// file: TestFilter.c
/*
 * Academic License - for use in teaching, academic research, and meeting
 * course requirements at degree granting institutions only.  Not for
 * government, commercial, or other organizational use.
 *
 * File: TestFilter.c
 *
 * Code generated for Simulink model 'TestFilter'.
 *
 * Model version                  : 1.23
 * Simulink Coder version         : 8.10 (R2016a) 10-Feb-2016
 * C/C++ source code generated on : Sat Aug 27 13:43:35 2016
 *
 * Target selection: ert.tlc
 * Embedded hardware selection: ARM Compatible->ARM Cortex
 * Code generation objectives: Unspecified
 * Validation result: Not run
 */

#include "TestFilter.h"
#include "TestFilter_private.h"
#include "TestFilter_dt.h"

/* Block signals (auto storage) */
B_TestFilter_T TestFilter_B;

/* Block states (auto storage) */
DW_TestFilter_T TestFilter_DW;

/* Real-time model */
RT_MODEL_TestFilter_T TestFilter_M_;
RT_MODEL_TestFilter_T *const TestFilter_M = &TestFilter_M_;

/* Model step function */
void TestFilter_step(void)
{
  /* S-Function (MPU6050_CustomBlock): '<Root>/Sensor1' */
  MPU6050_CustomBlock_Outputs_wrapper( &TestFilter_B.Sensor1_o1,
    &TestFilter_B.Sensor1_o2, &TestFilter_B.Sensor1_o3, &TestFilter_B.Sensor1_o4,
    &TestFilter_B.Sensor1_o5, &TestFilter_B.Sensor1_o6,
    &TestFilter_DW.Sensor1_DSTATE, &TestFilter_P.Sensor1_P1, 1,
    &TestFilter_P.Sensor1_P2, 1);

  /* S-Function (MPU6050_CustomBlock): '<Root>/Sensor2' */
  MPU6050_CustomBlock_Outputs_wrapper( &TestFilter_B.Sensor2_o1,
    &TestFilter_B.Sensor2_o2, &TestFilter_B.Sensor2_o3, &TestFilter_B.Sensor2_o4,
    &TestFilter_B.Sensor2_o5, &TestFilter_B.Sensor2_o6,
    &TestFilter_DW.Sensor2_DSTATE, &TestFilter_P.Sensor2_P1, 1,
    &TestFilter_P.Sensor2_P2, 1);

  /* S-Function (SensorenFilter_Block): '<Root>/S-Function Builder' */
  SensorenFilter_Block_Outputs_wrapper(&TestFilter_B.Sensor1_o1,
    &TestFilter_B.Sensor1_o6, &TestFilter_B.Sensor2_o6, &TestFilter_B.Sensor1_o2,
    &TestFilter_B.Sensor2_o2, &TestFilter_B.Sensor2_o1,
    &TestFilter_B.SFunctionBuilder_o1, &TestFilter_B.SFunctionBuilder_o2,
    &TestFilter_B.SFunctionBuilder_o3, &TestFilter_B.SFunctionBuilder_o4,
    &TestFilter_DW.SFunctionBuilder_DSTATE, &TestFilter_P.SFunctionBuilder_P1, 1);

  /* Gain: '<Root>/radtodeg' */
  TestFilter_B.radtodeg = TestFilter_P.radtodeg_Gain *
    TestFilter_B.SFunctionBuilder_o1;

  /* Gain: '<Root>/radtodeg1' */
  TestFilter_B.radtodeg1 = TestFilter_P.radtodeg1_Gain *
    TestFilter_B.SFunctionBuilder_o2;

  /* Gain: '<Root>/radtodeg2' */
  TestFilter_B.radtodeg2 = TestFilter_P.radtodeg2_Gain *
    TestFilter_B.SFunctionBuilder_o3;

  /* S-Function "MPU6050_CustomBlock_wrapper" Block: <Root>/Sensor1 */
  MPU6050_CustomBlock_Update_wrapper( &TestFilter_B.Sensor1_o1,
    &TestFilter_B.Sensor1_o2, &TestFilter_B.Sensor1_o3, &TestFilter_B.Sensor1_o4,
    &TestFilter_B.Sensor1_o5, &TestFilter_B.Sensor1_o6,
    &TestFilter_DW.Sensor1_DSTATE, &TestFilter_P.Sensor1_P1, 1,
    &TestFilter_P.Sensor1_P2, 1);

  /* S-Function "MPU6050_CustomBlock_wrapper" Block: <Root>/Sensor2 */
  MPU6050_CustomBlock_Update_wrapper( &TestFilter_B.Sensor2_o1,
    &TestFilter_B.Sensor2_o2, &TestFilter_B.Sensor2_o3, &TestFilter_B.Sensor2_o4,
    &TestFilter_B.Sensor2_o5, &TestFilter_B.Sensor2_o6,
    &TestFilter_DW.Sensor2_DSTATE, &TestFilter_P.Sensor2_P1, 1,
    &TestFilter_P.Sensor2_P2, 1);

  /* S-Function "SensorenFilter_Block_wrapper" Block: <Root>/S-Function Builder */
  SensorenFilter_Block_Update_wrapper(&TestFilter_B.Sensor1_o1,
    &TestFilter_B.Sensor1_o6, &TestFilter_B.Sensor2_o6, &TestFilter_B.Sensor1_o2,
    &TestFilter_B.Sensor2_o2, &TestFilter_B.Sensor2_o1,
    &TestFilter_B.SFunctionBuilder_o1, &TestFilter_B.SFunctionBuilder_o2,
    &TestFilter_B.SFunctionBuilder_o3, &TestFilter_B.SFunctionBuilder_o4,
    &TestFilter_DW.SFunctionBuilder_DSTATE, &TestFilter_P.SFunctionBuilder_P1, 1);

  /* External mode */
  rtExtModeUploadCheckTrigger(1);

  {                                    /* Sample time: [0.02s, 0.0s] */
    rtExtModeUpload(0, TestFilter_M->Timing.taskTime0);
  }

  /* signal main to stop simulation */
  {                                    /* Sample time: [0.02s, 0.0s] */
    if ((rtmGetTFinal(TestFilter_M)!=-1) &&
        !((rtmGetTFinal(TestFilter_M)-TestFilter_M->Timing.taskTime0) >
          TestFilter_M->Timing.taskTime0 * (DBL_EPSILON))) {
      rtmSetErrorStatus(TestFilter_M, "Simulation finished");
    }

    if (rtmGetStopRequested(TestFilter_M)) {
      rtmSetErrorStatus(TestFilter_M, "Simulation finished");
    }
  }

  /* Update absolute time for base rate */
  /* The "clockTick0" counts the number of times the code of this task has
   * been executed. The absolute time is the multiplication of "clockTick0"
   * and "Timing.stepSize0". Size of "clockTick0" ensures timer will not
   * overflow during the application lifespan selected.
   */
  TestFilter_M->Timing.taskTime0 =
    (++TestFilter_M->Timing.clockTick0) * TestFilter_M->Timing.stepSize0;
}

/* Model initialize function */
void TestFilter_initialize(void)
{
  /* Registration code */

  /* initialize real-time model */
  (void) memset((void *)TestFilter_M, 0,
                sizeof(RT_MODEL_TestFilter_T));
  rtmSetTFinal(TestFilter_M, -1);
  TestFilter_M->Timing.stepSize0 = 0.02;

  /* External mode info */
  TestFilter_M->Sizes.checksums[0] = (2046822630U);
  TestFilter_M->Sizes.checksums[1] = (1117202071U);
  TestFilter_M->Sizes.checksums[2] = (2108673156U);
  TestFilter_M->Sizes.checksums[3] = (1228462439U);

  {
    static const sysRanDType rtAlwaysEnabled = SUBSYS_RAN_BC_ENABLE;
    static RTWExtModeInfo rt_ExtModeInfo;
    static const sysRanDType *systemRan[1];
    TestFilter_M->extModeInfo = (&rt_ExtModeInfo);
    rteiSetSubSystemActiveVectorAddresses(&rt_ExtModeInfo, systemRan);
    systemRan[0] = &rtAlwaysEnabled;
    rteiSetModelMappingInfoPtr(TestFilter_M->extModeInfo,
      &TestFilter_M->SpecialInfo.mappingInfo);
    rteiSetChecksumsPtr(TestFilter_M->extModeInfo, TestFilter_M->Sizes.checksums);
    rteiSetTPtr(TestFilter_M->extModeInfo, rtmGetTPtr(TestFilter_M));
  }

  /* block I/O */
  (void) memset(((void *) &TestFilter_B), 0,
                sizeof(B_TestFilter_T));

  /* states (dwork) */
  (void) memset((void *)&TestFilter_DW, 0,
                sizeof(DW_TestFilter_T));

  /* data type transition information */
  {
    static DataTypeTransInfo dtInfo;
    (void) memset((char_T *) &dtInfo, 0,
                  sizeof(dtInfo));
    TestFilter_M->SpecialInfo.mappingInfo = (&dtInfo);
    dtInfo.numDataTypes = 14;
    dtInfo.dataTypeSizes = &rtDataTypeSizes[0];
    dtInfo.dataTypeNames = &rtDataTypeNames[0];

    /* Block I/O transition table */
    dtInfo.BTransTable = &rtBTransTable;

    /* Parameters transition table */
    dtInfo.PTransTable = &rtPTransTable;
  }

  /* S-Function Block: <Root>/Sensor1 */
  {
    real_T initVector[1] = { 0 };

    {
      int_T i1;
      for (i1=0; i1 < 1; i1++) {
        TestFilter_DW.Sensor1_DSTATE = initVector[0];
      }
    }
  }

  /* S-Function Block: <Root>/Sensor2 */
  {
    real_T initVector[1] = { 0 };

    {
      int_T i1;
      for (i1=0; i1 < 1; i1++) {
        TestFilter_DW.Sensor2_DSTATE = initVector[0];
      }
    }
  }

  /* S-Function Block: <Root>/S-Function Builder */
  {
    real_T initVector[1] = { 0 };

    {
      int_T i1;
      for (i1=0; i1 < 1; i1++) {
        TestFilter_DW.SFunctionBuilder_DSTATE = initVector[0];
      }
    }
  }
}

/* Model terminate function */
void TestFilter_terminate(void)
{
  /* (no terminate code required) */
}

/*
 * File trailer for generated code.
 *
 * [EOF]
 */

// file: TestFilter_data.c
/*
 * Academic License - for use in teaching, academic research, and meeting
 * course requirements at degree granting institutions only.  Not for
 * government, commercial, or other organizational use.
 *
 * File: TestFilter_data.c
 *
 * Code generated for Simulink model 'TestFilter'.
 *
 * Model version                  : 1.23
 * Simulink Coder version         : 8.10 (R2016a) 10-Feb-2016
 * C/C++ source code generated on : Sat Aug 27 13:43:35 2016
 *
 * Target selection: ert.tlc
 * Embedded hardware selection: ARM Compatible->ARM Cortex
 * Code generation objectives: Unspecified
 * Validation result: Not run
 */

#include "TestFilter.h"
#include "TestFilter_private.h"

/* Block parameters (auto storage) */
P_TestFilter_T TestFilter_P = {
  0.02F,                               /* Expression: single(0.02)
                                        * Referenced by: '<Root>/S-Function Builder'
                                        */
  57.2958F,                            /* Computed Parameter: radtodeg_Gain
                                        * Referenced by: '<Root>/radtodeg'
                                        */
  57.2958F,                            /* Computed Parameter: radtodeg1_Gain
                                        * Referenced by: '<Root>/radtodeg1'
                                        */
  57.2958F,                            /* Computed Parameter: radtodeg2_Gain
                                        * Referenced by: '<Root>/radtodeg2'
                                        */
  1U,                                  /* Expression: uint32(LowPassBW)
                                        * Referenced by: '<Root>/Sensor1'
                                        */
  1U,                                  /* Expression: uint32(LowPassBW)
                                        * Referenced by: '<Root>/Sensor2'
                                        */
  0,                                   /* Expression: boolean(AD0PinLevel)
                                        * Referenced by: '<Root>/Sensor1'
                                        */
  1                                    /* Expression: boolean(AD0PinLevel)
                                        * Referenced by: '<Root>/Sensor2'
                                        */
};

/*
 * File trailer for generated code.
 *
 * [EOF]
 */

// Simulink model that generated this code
simulink model "TestFilter"  (R2016a)
settings: Solver=FixedStepDiscrete  StartTime=0.0  StopTime=inf  FixedStep=0.02  RelTol=1e-3

== system TestFilter ==
  S-Function Builder : S-Function  InitFcn=try, set_param(gcb,'FunctionName','SensorenFilter_Block'), end  FunctionName=SensorenFilter_Block  Parameters=single(0.02)  SFunctionModules=SensorenFilter_Block_wrapper  SFunctionDeploymentMode=off  EnableBusSupport=off  mask(S-Function Builder){}
      mask help: Simulink:masks:SFunctionBuilder_MD
      mask init:
      | val = [[.9  0.75 0.75 1 1 .9 .9 1]',[1 1 0.75 0.75 .9 .9 1 .9]'];try , sys = get_param(gcb,'SfunBuilderFcnName');if isempty(sys), sys = get_param(gcb,'FunctionName'); end,catch, sys = get_param(gcb,'FunctionName'); end
  Scope1 : Scope  NumInputPorts=4
  Sensor1 : S-Function  InitFcn=try, set_param(gcb,'FunctionName','MPU6050_CustomBlock'), end  FunctionName=MPU6050_CustomBlock  Parameters=boolean(AD0PinLevel),uint32(LowPassBW)  SFunctionModules=MPU6050_CustomBlock_wrapper  SFunctionDeploymentMode=off  EnableBusSupport=off  mask(S-Function Builder){AD0PinLevel=0, LowPassBW=260}
      mask prompts: AD0PinLevel "Logic-Level of AD0 Pin"; LowPassBW "Low-Pass-Bandwidth [Hz]"
      mask help: Simulink:masks:SFunctionBuilder_MD
      mask init: same as TestFilter/S-Function Builder
  Sensor2 : S-Function  InitFcn=try, set_param(gcb,'FunctionName','MPU6050_CustomBlock'), end  FunctionName=MPU6050_CustomBlock  Parameters=boolean(AD0PinLevel),uint32(LowPassBW)  SFunctionModules=MPU6050_CustomBlock_wrapper  SFunctionDeploymentMode=off  EnableBusSupport=off  mask(S-Function Builder){AD0PinLevel=1, LowPassBW=260}
      mask prompts: AD0PinLevel "Logic-Level of AD0 Pin"; LowPassBW "Low-Pass-Bandwidth [Hz]"
      mask help: Simulink:masks:SFunctionBuilder_MD
      mask init: same as TestFilter/S-Function Builder
  Terminator{,1..5} (6 alike) : Terminator
  radtodeg : Gain  Gain=57.2958
  radtodeg1 : Gain  Gain=57.2958
  radtodeg2 : Gain  Gain=57.2958
  wires:
  Sensor1/3 -> Terminator5/1
  Sensor1/4 -> Terminator4/1
  Sensor1/5 -> Terminator3/1
  Sensor2/5 -> Terminator/1
  Sensor2/4 -> Terminator1/1
  Sensor2/3 -> Terminator2/1
  S-Function Builder/1 -> radtodeg/1
  S-Function Builder/2 -> radtodeg1/1
  S-Function Builder/3 -> radtodeg2/1
  S-Function Builder/4 -> Scope1/4
  radtodeg/1 -> Scope1/1
  radtodeg1/1 -> Scope1/2
  radtodeg2/1 -> Scope1/3
  Sensor1/1 -> S-Function Builder/1
  Sensor1/2 -> S-Function Builder/2
  Sensor1/6 -> S-Function Builder/3
  Sensor2/1 -> S-Function Builder/4
  Sensor2/2 -> S-Function Builder/5
  Sensor2/6 -> S-Function Builder/6
